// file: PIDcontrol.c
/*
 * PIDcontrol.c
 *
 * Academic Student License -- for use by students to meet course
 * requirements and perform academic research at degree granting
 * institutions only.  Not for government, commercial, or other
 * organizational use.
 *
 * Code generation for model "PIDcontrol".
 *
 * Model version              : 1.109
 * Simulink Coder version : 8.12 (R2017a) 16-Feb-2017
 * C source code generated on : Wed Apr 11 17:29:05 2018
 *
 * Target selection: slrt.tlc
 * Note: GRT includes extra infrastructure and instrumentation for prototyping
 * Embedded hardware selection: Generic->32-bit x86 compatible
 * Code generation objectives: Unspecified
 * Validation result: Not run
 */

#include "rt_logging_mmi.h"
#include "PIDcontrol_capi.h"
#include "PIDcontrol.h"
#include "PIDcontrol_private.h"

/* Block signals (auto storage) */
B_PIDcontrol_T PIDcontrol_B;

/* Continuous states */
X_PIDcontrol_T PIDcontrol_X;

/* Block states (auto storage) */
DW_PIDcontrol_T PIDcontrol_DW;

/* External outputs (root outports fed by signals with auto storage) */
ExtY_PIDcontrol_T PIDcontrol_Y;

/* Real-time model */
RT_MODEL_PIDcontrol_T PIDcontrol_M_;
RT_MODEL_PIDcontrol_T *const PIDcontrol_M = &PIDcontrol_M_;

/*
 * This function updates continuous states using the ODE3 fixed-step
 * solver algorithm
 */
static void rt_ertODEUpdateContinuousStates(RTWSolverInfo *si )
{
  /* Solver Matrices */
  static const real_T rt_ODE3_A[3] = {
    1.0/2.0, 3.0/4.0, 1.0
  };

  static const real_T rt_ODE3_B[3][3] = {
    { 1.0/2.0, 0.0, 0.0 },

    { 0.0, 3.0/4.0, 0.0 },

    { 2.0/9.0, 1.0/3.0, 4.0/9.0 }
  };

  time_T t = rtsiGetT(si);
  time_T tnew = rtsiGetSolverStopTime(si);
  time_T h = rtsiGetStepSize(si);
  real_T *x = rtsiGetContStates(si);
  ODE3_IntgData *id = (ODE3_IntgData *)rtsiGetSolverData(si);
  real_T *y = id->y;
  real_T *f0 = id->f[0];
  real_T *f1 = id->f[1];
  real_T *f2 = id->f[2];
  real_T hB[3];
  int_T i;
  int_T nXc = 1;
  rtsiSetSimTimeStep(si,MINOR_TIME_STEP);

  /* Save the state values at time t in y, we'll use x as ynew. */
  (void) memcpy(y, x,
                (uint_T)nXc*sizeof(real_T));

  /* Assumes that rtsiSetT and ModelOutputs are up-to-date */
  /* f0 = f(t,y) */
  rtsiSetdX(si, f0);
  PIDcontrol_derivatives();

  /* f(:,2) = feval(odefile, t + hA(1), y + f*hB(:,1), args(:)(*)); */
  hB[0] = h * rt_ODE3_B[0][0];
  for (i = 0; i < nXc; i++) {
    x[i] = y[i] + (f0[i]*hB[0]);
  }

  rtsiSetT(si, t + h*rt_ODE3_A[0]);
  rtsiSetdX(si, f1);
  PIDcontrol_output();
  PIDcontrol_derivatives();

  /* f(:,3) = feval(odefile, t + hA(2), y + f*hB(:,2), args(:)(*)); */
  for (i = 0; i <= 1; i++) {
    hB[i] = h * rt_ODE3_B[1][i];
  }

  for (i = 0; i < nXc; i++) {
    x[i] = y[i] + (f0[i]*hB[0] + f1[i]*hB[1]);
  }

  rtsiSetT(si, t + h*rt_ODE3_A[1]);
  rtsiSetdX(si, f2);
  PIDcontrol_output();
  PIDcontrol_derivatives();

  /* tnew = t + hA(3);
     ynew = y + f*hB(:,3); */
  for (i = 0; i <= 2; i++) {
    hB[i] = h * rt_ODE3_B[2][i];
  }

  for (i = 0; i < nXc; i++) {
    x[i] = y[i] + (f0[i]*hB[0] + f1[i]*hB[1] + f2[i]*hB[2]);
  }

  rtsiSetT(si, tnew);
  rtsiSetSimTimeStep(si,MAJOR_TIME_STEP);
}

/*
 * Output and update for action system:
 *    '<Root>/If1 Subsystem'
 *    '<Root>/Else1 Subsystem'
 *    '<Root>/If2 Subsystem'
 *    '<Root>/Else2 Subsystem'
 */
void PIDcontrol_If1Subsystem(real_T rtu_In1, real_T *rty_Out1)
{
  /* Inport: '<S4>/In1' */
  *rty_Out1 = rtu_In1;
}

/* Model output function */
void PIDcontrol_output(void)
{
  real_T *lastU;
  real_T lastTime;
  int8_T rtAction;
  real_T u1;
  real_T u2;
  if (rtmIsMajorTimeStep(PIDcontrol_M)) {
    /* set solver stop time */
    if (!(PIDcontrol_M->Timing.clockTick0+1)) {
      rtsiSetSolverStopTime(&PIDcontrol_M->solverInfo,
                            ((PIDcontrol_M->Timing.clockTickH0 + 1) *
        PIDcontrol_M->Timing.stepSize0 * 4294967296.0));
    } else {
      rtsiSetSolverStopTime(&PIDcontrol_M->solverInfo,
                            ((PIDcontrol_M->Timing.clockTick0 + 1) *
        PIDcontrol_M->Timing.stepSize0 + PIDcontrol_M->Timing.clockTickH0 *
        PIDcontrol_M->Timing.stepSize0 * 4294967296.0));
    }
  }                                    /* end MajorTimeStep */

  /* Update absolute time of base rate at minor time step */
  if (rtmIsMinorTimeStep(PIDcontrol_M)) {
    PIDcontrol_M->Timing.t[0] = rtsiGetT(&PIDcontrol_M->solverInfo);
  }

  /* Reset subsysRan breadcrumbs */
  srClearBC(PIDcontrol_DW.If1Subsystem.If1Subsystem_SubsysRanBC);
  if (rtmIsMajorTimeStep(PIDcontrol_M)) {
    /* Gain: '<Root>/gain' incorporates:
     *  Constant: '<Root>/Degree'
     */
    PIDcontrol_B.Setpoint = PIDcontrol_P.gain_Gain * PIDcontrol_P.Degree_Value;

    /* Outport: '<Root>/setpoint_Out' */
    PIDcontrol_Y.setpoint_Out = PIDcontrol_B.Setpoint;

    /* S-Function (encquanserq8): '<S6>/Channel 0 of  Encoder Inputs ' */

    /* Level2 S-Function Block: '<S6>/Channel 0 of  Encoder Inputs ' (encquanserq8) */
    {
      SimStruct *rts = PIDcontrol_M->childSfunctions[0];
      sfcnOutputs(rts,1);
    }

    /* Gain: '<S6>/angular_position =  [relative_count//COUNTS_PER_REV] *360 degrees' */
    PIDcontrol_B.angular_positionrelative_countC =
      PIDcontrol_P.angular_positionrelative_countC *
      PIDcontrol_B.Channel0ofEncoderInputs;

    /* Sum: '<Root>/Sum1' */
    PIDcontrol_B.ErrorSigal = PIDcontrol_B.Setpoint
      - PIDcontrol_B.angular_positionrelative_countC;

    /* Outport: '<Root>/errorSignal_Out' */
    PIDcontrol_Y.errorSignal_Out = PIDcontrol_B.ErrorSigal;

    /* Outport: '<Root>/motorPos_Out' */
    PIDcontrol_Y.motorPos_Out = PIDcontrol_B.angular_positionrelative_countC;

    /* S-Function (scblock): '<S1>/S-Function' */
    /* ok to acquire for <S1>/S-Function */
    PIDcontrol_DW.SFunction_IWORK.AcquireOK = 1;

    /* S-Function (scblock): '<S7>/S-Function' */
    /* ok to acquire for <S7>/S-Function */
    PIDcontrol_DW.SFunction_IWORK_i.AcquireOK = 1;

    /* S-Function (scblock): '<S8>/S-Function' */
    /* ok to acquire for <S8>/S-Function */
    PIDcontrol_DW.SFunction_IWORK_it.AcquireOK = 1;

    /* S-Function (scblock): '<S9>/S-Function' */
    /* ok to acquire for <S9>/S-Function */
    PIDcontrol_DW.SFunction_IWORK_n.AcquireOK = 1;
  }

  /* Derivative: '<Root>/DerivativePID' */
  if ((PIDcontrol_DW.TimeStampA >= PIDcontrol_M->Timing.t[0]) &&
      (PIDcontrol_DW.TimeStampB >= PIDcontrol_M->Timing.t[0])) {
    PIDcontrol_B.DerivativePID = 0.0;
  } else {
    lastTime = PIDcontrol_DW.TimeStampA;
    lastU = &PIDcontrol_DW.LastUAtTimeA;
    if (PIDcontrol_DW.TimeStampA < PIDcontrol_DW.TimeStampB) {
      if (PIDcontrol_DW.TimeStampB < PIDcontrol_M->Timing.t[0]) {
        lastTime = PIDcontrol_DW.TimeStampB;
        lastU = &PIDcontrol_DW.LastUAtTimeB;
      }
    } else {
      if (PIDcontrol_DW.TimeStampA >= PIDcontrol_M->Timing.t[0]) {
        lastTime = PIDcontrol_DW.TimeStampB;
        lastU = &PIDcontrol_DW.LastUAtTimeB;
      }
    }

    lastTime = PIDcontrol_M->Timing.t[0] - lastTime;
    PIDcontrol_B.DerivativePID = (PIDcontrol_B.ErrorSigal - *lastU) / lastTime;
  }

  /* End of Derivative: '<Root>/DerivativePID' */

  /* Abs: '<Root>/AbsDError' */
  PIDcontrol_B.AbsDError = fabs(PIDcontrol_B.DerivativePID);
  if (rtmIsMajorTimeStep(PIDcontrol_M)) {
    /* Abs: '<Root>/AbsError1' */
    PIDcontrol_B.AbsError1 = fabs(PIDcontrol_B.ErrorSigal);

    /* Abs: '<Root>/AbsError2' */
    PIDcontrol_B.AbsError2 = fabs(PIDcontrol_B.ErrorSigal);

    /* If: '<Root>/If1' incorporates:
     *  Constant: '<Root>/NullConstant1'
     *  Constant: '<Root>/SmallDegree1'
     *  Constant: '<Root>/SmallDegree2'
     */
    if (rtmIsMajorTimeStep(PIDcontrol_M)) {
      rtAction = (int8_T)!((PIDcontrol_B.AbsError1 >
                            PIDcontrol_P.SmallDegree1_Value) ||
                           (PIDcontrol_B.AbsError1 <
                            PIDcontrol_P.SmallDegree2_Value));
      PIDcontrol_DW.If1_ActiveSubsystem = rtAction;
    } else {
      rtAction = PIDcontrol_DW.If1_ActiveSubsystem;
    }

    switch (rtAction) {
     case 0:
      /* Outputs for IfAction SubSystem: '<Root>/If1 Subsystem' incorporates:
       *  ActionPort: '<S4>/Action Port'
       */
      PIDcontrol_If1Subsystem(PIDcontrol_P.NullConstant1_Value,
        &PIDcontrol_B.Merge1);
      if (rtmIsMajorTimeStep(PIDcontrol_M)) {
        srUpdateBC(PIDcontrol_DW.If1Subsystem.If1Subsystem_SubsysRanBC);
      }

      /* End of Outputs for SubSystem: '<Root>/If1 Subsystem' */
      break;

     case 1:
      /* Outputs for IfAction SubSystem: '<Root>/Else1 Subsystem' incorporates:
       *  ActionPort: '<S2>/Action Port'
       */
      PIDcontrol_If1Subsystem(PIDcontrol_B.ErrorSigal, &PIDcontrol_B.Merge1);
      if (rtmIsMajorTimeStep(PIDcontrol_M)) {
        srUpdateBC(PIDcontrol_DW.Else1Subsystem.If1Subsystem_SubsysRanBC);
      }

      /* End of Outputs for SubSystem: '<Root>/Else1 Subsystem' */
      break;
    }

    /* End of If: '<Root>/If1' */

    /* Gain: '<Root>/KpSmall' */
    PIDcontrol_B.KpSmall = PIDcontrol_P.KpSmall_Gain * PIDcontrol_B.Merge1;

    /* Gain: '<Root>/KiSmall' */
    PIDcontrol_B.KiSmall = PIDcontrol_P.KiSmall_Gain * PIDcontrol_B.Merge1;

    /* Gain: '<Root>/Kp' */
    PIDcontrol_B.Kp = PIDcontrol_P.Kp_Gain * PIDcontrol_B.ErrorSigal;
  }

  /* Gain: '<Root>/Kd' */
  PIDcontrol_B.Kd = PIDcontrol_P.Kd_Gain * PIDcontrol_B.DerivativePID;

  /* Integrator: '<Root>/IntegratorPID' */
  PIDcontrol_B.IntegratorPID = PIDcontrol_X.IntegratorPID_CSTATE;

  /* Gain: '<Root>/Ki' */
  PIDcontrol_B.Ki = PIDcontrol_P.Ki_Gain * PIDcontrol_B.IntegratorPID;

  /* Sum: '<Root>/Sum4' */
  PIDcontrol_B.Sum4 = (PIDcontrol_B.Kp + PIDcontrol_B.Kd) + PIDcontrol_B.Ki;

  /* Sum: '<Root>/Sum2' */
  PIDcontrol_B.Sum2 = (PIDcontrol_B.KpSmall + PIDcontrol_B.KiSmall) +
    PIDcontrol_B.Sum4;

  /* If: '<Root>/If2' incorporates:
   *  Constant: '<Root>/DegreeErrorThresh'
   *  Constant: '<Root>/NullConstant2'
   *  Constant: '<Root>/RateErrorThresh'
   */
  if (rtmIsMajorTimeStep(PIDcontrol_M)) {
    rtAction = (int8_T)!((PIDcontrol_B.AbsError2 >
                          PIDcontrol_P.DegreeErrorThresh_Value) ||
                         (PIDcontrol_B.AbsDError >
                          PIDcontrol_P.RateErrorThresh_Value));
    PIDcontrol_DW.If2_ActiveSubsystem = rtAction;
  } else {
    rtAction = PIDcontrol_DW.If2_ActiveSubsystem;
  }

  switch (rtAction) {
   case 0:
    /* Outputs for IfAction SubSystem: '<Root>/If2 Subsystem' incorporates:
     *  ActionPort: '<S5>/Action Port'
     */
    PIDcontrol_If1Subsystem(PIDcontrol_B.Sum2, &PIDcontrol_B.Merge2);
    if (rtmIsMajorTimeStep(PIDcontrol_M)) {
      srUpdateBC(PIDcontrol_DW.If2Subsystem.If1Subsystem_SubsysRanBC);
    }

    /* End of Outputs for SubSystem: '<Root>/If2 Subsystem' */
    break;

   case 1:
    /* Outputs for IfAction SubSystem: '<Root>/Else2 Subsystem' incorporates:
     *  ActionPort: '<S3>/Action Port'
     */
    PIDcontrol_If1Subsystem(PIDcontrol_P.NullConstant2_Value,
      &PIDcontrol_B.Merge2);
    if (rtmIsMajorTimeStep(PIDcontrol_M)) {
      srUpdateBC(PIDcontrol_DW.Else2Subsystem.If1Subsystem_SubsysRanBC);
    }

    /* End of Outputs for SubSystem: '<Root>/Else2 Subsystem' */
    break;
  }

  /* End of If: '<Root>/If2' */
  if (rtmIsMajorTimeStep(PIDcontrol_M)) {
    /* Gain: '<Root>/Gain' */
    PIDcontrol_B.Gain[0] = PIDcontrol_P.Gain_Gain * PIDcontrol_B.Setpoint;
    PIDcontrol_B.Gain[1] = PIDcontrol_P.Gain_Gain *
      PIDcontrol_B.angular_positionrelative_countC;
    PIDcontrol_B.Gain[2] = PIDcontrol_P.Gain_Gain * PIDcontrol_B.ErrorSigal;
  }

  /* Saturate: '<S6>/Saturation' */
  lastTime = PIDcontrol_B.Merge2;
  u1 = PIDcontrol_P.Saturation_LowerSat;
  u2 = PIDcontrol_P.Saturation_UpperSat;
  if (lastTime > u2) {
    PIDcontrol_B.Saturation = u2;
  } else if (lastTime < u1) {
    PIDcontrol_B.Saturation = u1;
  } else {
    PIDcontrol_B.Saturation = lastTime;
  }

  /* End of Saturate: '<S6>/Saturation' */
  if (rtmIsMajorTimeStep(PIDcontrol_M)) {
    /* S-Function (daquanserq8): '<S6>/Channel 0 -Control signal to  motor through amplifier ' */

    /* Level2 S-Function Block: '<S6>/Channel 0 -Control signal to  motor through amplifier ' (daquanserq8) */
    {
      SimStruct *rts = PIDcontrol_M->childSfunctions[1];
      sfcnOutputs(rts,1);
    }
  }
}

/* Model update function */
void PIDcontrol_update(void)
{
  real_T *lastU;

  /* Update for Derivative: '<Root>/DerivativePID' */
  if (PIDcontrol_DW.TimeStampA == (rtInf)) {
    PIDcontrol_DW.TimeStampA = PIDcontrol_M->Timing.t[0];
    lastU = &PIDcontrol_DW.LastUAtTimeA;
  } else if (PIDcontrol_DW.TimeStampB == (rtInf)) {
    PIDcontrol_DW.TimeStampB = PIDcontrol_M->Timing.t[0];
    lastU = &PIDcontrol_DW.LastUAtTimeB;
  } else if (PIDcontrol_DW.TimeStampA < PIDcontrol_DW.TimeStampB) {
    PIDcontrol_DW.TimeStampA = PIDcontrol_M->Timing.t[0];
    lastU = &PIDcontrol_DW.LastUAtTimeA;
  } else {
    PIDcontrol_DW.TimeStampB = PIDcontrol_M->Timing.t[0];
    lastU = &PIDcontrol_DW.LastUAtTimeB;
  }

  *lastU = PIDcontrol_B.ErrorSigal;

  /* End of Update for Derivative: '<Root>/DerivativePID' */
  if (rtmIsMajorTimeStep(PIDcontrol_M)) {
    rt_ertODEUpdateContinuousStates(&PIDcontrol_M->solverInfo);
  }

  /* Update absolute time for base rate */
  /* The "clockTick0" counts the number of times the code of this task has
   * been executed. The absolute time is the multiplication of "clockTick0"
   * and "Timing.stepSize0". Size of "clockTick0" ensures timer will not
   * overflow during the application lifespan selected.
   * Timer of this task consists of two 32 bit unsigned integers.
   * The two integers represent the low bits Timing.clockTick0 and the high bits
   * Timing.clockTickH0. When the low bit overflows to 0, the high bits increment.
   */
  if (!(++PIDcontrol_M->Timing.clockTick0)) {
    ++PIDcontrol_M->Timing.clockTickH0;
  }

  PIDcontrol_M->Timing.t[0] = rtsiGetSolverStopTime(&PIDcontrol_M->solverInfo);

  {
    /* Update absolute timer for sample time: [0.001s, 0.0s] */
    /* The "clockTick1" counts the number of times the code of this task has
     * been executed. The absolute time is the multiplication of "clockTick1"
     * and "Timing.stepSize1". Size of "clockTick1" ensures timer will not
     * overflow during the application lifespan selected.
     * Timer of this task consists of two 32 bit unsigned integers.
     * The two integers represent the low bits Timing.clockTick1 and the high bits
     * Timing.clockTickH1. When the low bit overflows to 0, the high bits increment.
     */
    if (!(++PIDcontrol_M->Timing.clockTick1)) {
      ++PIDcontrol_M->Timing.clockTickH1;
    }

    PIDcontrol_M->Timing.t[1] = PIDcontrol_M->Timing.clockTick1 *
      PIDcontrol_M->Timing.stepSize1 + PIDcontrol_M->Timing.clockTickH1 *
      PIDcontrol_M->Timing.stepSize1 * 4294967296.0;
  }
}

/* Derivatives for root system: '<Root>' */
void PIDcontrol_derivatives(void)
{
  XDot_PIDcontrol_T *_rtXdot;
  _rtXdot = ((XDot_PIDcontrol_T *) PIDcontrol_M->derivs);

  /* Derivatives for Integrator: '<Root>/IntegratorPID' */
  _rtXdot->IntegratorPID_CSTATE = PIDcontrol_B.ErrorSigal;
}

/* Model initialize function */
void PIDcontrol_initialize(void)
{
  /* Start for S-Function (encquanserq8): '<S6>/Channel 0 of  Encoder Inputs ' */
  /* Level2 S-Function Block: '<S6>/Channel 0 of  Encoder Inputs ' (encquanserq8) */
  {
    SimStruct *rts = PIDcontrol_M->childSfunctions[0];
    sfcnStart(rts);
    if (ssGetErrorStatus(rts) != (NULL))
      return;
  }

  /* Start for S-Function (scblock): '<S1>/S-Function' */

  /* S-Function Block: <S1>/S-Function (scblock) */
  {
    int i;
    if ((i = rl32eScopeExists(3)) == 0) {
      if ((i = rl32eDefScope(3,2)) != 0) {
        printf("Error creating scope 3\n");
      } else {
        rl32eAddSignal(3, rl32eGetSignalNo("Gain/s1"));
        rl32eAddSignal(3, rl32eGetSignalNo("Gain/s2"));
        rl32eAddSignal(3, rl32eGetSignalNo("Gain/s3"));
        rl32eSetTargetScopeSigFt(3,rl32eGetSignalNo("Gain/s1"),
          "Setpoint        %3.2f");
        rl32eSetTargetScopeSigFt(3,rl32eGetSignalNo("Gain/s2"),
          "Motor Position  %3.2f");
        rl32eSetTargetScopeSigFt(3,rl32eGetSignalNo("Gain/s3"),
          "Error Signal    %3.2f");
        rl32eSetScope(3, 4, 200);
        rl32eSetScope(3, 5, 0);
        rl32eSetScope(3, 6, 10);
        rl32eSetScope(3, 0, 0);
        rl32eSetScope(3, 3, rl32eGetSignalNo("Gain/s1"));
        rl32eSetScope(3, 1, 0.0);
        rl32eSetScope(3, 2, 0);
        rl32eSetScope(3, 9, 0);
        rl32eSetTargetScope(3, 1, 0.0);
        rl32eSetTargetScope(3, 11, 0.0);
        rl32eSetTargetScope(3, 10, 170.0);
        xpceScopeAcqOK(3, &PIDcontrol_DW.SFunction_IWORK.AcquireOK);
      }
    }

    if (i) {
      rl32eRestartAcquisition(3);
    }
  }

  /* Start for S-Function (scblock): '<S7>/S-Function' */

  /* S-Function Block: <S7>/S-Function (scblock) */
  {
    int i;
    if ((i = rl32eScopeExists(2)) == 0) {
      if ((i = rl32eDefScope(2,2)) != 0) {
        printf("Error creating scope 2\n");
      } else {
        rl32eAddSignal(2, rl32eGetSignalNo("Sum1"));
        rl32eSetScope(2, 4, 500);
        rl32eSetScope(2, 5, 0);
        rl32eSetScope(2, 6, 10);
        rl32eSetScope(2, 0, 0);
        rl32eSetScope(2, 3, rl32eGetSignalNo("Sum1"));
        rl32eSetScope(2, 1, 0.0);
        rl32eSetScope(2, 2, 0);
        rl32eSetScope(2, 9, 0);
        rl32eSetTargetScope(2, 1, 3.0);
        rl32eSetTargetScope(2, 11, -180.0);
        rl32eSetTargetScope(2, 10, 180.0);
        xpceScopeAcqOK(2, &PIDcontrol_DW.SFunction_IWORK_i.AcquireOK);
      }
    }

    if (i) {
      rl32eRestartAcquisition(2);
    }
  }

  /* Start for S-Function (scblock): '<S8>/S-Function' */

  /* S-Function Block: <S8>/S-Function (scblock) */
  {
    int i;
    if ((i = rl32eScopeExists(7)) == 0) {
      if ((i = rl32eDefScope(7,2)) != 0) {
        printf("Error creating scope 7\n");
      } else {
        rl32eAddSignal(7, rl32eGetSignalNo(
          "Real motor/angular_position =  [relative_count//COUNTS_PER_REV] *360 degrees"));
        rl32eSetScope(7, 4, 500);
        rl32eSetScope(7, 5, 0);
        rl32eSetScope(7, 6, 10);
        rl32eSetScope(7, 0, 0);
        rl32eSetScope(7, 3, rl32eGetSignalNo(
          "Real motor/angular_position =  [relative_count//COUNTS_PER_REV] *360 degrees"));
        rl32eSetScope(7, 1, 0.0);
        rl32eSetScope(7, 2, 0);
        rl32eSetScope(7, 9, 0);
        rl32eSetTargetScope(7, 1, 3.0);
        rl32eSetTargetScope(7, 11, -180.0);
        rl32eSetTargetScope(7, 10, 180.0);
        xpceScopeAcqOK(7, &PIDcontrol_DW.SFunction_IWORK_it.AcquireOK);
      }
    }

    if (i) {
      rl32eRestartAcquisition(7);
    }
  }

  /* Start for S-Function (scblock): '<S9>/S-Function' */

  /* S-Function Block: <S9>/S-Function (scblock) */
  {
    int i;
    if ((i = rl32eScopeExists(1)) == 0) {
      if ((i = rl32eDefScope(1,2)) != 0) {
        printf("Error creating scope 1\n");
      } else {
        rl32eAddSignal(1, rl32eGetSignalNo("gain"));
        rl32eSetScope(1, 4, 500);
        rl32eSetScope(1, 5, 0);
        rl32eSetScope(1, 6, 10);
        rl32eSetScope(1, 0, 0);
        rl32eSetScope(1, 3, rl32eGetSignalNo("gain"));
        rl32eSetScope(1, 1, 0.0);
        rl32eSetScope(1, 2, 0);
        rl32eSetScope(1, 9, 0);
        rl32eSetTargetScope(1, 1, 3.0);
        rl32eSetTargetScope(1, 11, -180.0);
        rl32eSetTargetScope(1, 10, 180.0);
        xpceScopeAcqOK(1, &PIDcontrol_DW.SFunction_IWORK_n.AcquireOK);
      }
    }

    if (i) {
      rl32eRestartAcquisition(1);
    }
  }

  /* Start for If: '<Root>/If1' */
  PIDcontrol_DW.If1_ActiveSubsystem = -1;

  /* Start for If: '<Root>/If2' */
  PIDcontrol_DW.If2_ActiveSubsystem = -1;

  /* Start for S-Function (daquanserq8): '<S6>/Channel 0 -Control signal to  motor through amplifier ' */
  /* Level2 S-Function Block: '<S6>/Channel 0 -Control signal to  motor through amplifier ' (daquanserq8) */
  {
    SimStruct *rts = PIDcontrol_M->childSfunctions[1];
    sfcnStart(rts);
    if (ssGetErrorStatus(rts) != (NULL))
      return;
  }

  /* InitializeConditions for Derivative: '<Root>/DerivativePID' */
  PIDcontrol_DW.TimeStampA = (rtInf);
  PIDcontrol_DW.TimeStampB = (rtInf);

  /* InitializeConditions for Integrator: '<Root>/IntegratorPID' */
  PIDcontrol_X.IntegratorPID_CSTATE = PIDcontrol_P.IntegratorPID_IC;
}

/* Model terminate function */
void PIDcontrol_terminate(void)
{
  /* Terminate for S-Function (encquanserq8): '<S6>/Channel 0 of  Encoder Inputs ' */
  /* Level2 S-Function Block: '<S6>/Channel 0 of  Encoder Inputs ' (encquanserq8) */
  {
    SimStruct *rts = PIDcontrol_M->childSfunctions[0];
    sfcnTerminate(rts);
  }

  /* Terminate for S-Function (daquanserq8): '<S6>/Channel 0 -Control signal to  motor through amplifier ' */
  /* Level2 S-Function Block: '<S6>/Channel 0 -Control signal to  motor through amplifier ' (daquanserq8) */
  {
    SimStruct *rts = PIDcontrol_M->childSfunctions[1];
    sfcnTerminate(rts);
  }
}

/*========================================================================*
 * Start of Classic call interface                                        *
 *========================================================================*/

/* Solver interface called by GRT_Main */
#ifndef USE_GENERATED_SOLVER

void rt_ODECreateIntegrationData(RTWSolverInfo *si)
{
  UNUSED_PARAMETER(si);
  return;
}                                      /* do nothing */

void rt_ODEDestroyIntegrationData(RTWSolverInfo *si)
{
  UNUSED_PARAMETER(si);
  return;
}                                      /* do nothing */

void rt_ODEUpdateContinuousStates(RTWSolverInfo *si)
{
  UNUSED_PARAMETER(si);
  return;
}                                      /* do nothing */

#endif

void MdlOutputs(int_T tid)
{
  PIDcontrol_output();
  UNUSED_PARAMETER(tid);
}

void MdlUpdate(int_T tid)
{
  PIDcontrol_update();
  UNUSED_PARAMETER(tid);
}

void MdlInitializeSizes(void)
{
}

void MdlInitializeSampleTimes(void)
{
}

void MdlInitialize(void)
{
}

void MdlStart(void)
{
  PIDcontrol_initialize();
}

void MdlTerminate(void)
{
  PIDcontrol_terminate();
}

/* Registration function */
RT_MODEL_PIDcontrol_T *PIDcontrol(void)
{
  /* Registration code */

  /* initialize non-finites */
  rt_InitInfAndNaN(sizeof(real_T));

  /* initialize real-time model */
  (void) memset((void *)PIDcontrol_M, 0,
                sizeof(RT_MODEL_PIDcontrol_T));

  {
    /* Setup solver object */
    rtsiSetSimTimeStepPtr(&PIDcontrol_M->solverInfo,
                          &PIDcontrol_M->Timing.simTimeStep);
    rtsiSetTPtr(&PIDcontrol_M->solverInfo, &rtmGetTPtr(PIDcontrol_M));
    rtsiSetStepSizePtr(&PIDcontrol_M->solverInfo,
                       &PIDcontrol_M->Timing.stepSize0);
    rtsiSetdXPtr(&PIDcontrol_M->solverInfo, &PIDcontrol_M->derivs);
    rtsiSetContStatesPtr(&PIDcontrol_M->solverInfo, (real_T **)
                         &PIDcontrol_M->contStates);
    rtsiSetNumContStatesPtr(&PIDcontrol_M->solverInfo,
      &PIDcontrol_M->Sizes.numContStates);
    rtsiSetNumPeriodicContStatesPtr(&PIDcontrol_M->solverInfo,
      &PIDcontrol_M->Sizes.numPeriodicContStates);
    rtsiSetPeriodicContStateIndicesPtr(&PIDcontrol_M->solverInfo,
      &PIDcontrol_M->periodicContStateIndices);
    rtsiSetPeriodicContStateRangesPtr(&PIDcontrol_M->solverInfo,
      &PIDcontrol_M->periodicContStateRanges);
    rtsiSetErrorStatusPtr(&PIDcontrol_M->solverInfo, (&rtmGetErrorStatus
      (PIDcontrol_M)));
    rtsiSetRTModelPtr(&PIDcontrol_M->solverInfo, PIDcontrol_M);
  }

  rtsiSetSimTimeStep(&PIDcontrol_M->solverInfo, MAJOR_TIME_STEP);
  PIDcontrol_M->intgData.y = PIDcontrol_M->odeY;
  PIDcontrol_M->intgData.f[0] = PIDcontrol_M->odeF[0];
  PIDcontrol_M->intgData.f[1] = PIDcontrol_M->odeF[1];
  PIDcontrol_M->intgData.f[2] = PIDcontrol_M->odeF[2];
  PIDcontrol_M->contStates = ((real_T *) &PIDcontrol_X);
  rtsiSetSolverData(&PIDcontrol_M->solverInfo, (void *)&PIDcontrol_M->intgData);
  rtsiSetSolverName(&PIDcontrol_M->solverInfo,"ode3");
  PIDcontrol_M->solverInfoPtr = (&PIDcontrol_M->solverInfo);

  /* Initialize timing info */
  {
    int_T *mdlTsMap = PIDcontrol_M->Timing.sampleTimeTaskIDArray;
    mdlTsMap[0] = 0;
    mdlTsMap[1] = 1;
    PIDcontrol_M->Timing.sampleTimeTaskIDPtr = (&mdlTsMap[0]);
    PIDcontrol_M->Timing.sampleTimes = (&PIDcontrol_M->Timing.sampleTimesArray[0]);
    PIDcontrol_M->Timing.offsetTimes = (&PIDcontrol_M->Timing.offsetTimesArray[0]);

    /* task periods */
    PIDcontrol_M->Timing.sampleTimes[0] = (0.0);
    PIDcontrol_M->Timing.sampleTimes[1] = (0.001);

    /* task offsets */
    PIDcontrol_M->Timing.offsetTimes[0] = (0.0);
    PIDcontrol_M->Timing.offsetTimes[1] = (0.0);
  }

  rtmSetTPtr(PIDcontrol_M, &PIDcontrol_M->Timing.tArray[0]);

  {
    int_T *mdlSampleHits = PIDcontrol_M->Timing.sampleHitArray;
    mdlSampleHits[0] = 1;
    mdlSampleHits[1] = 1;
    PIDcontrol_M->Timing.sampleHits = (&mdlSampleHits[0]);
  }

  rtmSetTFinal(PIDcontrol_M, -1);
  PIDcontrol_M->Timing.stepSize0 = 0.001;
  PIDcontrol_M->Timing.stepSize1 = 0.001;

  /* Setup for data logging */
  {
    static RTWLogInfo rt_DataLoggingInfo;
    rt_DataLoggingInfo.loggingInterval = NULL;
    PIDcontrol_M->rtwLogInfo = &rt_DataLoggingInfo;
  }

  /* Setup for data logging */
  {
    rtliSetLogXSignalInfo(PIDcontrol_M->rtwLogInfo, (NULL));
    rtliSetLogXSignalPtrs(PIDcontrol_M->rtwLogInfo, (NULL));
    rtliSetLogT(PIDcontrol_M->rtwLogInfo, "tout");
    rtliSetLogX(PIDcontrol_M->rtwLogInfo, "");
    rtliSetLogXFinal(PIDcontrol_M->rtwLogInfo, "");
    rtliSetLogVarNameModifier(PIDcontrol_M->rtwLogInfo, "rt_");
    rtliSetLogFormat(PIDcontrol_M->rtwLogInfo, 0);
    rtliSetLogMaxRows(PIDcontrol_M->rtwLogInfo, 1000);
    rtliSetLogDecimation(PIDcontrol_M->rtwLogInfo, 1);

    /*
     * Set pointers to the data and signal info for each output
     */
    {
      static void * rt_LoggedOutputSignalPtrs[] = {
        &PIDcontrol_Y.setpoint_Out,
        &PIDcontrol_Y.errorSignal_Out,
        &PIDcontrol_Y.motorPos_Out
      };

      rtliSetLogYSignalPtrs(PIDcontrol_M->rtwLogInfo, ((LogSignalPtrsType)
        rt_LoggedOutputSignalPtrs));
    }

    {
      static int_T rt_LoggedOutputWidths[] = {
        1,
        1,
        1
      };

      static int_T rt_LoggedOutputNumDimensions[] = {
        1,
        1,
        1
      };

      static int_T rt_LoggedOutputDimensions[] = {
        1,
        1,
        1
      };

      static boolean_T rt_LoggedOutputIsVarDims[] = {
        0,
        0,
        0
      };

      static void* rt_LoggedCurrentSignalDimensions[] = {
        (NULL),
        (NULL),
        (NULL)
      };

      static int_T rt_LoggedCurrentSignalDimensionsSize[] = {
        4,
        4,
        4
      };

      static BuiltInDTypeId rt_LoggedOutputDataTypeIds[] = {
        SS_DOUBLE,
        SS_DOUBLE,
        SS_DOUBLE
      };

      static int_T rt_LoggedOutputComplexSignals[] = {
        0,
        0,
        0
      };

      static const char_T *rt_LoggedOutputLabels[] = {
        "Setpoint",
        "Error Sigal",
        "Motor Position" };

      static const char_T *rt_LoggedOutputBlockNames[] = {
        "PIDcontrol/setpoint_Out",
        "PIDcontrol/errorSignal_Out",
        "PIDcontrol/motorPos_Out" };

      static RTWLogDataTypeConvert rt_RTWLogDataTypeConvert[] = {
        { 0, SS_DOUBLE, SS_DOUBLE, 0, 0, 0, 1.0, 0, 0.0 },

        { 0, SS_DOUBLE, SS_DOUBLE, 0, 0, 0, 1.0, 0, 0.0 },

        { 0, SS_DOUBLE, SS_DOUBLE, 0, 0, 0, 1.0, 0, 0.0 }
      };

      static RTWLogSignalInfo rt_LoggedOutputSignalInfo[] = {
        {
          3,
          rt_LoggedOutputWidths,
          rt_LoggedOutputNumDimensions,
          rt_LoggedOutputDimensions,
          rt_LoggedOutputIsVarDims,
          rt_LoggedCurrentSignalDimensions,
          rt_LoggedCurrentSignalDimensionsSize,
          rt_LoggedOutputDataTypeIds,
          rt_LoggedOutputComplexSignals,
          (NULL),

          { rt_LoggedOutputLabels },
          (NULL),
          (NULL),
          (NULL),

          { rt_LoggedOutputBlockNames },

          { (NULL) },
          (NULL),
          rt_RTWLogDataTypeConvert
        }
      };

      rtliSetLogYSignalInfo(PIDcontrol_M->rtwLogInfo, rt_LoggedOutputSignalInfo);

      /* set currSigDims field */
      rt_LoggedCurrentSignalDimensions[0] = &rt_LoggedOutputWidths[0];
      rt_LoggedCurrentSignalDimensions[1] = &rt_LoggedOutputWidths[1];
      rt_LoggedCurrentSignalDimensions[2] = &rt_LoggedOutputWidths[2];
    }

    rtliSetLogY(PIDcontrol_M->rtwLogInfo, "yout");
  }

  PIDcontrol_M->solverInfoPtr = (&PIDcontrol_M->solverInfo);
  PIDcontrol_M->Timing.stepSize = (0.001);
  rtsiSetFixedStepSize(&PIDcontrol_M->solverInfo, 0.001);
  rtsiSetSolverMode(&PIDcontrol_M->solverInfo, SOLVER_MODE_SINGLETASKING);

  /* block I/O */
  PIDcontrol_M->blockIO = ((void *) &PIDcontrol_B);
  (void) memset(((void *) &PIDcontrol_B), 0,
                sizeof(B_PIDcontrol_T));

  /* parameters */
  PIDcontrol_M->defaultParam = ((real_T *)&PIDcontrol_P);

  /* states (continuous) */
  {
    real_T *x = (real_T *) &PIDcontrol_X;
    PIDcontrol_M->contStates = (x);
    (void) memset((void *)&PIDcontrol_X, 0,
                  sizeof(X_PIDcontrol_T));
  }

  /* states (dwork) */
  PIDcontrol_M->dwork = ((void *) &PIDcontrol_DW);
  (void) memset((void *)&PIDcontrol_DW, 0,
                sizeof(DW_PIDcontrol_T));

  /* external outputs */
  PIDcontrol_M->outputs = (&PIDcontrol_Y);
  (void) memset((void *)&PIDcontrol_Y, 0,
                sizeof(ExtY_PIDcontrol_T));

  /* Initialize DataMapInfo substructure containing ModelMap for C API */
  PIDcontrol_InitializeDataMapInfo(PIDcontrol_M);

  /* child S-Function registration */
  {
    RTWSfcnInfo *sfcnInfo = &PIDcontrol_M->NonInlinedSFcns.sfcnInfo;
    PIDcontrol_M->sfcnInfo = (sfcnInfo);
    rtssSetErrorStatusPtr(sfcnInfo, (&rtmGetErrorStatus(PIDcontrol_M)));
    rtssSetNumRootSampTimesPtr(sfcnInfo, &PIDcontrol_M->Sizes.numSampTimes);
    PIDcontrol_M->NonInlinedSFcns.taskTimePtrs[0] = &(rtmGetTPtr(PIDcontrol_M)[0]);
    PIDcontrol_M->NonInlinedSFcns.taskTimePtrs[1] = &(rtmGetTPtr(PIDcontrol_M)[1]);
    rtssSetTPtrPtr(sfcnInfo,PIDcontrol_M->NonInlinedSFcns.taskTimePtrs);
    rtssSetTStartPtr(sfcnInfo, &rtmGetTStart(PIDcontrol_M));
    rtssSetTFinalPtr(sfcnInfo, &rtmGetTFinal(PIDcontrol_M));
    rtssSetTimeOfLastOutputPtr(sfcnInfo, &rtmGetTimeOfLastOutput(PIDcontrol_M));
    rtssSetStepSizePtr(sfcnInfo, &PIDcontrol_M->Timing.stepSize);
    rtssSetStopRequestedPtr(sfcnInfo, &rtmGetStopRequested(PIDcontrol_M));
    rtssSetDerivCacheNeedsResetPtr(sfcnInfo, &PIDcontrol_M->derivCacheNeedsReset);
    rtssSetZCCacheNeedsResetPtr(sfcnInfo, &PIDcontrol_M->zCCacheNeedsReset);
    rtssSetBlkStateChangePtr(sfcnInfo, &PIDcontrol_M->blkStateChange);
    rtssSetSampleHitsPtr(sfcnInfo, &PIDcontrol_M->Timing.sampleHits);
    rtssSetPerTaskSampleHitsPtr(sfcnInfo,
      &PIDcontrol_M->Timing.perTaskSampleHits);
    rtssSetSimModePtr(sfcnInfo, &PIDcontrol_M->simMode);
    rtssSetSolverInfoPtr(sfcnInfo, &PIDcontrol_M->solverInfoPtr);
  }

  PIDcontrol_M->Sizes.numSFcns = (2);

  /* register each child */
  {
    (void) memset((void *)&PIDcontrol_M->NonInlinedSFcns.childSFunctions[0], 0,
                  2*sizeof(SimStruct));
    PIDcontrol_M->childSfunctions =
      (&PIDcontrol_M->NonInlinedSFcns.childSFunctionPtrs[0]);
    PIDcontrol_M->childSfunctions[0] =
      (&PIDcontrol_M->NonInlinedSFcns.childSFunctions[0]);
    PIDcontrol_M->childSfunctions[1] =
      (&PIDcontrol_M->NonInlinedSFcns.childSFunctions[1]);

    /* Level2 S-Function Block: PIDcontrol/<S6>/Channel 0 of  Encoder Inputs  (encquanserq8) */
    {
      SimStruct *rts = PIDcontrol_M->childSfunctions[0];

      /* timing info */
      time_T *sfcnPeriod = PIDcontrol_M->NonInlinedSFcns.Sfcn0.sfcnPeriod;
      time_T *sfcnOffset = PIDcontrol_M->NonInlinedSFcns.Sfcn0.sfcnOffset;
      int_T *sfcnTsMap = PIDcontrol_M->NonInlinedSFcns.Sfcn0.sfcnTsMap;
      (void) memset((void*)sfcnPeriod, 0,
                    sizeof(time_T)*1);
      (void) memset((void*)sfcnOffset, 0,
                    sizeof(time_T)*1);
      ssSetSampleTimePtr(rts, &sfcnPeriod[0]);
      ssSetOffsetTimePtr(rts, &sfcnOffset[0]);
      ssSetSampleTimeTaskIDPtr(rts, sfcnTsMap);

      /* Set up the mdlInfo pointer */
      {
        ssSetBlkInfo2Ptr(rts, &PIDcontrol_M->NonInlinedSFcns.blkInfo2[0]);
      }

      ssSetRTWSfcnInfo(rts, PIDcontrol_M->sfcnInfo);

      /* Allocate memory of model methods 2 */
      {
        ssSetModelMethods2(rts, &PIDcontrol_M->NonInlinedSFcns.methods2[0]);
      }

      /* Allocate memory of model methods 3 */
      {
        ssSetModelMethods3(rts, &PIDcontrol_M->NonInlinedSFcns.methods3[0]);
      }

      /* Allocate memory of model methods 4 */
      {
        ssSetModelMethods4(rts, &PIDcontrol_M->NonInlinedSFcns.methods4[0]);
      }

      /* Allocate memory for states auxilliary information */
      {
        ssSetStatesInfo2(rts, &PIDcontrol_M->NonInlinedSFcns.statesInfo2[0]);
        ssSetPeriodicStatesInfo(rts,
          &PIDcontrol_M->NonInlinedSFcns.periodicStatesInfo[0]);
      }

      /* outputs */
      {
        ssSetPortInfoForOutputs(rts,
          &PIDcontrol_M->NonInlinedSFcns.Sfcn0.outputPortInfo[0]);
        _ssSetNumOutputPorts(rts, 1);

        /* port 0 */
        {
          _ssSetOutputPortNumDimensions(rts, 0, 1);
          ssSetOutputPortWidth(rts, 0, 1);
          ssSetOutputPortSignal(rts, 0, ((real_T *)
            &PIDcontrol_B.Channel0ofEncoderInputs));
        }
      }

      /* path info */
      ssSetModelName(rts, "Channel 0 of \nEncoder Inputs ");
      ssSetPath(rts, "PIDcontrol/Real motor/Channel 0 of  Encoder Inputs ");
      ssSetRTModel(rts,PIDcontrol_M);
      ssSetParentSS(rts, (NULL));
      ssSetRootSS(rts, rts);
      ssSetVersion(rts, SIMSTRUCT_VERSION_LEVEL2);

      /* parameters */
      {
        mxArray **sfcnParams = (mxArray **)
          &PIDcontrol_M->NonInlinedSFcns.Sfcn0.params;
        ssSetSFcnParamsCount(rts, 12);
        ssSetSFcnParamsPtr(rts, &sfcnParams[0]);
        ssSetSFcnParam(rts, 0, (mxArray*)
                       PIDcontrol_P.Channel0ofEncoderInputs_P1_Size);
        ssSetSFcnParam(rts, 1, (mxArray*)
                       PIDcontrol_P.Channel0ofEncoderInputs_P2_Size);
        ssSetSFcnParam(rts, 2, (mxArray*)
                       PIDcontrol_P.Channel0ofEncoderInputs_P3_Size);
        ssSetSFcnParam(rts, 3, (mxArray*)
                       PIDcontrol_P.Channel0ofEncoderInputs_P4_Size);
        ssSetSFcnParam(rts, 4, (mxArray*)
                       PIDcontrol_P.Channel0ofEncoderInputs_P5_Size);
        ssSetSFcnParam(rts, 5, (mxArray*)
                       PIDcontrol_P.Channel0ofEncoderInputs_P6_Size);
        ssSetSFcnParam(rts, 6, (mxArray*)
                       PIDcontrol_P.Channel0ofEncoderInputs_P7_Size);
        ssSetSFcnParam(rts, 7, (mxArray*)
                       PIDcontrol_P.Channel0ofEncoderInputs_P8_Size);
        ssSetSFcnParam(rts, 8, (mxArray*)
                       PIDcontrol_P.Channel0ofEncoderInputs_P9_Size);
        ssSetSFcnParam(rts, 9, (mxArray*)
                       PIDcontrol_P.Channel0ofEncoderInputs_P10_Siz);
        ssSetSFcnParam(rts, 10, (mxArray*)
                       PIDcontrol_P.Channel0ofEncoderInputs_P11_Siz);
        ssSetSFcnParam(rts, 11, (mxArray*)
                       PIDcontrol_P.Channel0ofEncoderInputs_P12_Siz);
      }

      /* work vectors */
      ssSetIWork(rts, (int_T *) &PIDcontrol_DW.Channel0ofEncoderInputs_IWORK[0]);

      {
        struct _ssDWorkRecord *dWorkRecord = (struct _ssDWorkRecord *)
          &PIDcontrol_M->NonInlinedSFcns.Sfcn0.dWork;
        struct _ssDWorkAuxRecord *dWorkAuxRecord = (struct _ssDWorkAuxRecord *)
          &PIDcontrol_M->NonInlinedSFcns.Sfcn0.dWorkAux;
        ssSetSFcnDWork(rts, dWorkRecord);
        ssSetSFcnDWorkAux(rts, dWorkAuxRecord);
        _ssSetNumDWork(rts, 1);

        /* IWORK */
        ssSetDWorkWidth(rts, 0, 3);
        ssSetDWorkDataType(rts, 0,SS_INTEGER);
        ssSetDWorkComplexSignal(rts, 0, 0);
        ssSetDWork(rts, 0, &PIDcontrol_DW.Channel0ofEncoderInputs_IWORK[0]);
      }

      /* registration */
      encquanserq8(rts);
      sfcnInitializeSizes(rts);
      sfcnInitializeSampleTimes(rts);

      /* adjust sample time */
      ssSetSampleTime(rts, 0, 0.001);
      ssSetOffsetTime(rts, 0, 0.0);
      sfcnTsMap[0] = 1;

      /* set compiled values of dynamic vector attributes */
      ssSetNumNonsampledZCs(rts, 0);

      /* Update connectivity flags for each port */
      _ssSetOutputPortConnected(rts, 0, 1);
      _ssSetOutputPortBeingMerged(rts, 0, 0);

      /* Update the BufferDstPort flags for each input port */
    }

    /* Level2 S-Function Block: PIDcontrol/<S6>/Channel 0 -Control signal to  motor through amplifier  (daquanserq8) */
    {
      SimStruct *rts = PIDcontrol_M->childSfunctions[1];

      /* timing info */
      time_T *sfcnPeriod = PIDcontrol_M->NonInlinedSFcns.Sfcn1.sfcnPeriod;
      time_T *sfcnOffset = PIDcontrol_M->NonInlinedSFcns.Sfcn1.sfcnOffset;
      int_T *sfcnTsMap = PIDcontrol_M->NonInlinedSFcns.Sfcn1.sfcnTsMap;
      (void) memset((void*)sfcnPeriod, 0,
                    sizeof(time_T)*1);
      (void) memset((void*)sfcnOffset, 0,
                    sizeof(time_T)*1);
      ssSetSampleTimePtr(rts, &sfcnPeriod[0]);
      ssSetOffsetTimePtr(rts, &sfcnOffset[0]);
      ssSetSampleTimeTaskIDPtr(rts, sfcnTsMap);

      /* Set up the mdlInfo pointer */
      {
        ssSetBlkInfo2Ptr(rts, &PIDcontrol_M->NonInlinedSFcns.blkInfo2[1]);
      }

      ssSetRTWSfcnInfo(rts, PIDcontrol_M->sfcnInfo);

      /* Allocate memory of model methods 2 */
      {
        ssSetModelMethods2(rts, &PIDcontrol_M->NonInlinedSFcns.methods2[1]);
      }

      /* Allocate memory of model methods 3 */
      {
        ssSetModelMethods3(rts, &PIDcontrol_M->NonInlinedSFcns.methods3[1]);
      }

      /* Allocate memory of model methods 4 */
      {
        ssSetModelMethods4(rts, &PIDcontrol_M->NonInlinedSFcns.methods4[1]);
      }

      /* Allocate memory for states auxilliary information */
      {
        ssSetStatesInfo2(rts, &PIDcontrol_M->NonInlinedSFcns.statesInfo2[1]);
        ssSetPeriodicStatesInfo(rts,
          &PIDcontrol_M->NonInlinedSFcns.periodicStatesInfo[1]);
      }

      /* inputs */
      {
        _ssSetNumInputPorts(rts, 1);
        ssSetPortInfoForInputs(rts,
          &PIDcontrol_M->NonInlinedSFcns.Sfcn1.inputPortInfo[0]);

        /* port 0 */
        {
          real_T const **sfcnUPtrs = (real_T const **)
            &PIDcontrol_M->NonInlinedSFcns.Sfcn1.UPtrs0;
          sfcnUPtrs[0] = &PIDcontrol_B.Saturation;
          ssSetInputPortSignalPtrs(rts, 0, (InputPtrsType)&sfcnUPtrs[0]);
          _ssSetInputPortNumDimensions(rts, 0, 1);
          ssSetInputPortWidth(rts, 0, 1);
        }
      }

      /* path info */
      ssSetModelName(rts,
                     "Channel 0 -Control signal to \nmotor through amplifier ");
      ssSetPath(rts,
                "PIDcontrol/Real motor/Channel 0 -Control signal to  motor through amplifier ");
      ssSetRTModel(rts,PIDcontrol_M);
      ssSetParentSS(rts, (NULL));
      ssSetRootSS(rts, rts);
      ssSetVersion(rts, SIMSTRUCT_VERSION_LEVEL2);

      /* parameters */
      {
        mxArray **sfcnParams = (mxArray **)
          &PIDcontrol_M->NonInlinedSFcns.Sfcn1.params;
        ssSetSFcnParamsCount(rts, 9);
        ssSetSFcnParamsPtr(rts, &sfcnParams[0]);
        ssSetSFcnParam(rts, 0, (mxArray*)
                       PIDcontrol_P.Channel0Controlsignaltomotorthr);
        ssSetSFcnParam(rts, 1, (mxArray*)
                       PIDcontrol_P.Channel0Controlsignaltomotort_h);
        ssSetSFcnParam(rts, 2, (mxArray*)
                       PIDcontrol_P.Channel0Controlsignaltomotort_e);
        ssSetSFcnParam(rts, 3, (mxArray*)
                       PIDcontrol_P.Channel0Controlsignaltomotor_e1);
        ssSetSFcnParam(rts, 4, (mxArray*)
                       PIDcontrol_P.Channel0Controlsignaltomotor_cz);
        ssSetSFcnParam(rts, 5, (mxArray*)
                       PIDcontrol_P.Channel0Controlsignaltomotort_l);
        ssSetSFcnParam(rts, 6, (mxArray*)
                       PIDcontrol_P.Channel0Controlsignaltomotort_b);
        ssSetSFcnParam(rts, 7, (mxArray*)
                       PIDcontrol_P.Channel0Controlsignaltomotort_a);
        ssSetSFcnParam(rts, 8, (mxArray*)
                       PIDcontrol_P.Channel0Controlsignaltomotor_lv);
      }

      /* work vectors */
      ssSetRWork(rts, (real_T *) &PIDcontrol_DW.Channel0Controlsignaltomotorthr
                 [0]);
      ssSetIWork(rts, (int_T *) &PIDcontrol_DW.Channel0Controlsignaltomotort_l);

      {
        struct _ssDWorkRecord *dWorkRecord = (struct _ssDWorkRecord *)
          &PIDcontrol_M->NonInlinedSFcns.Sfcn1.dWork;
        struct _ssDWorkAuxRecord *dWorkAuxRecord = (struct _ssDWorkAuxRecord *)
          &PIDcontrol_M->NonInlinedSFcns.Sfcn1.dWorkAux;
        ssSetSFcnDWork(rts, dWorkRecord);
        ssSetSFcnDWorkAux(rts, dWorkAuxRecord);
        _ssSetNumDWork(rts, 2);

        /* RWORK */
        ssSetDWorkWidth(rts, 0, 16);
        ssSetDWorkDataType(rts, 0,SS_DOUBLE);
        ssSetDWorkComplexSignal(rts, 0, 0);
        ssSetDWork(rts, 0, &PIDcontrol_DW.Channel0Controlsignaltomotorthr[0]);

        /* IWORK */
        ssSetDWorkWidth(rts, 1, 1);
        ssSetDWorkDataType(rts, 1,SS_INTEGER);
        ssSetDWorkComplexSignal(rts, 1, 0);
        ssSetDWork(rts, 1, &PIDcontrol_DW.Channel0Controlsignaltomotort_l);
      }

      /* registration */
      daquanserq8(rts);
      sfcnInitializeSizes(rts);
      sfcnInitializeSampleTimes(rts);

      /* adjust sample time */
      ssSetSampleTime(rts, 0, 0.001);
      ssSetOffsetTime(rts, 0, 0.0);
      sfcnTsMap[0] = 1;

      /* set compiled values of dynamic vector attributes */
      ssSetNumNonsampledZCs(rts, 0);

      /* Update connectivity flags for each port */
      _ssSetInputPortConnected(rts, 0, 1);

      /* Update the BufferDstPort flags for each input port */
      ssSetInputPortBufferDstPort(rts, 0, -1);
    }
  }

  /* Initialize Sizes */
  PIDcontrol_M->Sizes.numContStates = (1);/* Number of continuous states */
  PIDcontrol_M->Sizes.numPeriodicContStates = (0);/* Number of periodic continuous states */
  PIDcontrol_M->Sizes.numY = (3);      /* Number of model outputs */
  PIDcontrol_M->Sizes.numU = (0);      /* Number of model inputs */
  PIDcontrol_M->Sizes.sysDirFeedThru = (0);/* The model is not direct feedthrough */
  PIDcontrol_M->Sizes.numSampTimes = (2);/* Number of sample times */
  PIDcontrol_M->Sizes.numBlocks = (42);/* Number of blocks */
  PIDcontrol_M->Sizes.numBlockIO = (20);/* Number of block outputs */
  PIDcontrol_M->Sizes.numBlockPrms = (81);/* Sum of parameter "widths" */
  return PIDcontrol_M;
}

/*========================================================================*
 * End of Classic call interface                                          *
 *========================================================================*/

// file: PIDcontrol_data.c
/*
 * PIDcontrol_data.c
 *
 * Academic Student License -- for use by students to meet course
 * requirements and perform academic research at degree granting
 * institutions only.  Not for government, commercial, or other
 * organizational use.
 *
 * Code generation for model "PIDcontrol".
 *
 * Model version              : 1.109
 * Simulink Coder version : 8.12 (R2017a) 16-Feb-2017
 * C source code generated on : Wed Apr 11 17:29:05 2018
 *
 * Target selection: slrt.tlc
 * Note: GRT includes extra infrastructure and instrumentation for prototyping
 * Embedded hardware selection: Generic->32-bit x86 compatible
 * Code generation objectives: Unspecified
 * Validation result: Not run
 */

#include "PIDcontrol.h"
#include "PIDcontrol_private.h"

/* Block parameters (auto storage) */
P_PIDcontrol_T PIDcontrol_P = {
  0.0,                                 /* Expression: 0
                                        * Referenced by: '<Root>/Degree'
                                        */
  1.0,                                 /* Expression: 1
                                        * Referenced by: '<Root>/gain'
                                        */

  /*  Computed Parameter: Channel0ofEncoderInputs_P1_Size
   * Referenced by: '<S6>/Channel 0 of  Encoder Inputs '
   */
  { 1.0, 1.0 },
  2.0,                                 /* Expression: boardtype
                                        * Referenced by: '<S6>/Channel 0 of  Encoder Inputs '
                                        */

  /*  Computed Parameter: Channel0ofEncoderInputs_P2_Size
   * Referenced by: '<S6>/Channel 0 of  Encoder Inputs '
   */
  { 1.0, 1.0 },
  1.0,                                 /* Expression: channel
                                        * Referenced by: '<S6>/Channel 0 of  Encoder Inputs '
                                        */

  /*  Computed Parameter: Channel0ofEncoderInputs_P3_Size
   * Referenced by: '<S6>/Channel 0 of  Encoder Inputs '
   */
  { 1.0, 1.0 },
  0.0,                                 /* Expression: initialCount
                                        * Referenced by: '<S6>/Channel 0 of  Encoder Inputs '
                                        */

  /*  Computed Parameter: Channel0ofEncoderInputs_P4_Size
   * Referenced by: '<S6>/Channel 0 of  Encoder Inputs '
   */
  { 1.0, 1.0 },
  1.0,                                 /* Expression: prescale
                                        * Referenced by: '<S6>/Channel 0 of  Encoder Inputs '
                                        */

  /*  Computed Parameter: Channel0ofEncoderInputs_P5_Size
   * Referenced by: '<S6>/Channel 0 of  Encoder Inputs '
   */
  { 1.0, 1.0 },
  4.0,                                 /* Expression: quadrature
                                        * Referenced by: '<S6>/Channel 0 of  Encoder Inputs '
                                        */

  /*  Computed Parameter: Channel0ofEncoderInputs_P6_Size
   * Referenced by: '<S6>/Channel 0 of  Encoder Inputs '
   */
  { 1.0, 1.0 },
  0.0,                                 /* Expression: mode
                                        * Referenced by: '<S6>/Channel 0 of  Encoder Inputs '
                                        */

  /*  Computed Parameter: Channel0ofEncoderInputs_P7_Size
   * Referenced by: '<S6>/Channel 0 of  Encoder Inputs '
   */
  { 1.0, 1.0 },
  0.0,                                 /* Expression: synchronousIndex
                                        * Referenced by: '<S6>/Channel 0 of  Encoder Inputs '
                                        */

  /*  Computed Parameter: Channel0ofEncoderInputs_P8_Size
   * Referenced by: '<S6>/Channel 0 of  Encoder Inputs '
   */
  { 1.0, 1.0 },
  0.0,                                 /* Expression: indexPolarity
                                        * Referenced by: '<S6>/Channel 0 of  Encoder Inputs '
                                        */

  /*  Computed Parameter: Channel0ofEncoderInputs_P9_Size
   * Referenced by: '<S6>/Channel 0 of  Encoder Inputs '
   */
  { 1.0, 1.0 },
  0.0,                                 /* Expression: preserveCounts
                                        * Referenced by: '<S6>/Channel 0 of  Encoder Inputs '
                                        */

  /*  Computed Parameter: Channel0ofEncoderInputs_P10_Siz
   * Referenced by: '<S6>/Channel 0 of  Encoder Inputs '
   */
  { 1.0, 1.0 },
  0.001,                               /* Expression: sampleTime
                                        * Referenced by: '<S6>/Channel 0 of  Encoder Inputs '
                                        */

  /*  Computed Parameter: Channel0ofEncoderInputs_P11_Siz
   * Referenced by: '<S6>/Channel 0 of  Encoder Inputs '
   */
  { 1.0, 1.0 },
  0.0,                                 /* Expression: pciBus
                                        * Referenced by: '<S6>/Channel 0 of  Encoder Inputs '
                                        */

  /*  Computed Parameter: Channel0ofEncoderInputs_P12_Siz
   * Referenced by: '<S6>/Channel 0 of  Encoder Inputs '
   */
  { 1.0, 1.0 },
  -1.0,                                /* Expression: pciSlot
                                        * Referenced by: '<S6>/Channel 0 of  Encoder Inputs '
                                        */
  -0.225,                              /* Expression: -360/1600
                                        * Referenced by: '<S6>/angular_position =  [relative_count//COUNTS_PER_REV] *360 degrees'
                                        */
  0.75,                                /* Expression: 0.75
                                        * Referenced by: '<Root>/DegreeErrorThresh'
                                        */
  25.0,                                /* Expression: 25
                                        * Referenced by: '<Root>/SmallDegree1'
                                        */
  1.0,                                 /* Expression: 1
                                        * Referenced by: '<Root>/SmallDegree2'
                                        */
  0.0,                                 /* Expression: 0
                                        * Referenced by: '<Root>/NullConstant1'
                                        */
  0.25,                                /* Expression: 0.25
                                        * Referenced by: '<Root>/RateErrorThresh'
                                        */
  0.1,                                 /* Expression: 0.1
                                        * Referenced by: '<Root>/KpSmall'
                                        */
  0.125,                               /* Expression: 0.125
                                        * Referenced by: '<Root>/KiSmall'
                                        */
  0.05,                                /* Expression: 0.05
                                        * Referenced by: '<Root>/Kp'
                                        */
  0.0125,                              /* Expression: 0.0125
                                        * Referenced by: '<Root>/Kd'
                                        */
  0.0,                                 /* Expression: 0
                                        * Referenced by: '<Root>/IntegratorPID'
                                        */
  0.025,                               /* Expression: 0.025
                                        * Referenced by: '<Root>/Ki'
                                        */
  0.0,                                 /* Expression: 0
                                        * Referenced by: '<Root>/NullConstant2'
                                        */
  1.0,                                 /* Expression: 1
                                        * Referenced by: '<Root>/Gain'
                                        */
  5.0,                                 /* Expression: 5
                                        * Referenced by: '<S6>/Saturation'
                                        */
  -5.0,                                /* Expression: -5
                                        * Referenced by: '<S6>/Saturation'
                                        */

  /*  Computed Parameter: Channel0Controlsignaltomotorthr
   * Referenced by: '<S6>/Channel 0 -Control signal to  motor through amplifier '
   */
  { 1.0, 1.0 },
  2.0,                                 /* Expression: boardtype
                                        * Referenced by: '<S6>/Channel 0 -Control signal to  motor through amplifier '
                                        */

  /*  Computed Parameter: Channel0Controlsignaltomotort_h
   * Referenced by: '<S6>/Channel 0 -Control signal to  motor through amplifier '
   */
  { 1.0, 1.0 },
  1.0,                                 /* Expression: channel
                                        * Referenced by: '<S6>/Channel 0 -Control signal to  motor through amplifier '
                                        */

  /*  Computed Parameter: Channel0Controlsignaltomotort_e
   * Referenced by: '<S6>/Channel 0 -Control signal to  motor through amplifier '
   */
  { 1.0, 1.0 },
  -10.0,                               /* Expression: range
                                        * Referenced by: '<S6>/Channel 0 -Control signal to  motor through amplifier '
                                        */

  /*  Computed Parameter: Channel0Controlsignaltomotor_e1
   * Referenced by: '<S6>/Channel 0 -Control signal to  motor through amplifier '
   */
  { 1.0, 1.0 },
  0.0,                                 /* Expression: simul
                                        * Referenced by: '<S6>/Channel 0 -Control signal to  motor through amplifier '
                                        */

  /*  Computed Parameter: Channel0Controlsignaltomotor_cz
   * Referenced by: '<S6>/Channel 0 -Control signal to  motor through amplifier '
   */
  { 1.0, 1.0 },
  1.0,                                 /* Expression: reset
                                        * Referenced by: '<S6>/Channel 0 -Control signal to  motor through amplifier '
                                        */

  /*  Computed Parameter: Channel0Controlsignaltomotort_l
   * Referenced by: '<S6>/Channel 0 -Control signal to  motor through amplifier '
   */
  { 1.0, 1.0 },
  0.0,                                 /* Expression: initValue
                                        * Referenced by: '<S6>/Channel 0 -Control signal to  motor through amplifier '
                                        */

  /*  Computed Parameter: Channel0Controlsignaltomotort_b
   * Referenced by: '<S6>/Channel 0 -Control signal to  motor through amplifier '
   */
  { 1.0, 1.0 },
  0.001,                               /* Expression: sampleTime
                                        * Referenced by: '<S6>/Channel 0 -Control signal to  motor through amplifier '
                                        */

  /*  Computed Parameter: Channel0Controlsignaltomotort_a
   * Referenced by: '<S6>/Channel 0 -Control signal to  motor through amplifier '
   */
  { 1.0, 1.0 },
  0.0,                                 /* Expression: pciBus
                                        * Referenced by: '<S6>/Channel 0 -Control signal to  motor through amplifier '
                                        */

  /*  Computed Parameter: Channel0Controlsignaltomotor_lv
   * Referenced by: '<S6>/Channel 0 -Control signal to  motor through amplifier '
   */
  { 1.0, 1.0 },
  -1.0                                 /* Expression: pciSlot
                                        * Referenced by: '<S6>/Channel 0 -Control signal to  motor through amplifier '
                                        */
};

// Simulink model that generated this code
simulink model "PIDcontrol"  (Simulink 8.9)
settings: Solver=ode3  StartTime=0.0  StopTime=inf  FixedStep=0.001  RelTol=1e-3  EnableMultiTasking=on
libraries: slrtlib x4, xpcquanserlib x2

== system PIDcontrol ==
  AbsDError : Abs
  AbsError1 : Abs
  AbsError2 : Abs
  Data Display : slrtlib/Displays and Logging/Scope   scopeno=3  scopetype=Target  autostart=on  viewmode=Numerical  formatstr="'Setpoint        %3.2f,Motor Position  %3.2f,Error Signal    %3.2f'"  grid=on  ylimits=[0,170]  nosamples=200  noprepostsamples=0  interleave=10  triggermode=FreeRun  triggersignal=1  trigsignalfromport=off  triggerlevel=0.0  triggerslope=Either  triggerscope=1  triggersample=0  filename=data.dat  mode=Lazy  writesize=512  autorestart=off  dynamicfilemode=off  maxwritefilesize=512*1024^2
  Degree : Constant  Value=0
  DegreeErrorThresh : Constant  Value=0.75
  DerivativePID : Derivative
  Else1 Subsystem : Subsystem  TreatAsAtomicUnit=on
  Else2 Subsystem : Subsystem  TreatAsAtomicUnit=on
  Gain : Gain
  If1 : If  NumInputs=3  IfExpression=u1 > u2 | u1 < u3
  If1 Subsystem : Subsystem  TreatAsAtomicUnit=on
  If2 : If  NumInputs=4  IfExpression=u1 > u2 | u3 > u4
  If2 Subsystem : Subsystem  TreatAsAtomicUnit=on
  IntegratorPID : Integrator
  Kd : Gain  Gain=0.0125
  Ki : Gain  Gain=0.025
  KiSmall : Gain  Gain=0.125
  Kp : Gain  Gain=0.05
  KpSmall : Gain  Gain=0.1
  Merge1 : Merge
  Merge2 : Merge
  Mux : Mux  Inputs=3
  NullConstant1 : Constant  Value=0
  NullConstant2 : Constant  Value=0
  RateErrorThresh : Constant  Value=0.25
  Real motor : Subsystem
  SmallDegree1 : Constant  Value=25
  SmallDegree2 : Constant
  Sum1 : Sum  Inputs=|+-
  Sum2 : Sum  Inputs=||+++
  Sum4 : Sum  Inputs=||+++
  error signal : slrtlib/Displays and Logging/Scope   scopeno=2  scopetype=Target  autostart=on  viewmode=Graphical rolling  formatstr='%15.6f'  grid=on  ylimits=[-180,180]  nosamples=500  noprepostsamples=0  interleave=10  triggermode=FreeRun  triggersignal=1  trigsignalfromport=off  triggerlevel=0.0  triggerslope=Either  triggerscope=1  triggersample=0  filename=data.dat  mode=Lazy  writesize=512  autorestart=off  dynamicfilemode=off  maxwritefilesize=512*1024^2
  gain : Gain
  motor position : slrtlib/Displays and Logging/Scope   scopeno=7  scopetype=Target  autostart=on  viewmode=Graphical rolling  formatstr='%15.6f'  grid=on  ylimits=[-180,180]  nosamples=500  noprepostsamples=0  interleave=10  triggermode=FreeRun  triggersignal=1  trigsignalfromport=off  triggerlevel=0.0  triggerslope=Either  triggerscope=1  triggersample=0  filename=data.dat  mode=Lazy  writesize=512  autorestart=off  dynamicfilemode=off  maxwritefilesize=512*1024^2
  setpoint : slrtlib/Displays and Logging/Scope   scopeno=1  scopetype=Target  autostart=on  viewmode=Graphical rolling  formatstr='%15.6f'  grid=on  ylimits=[-180,180]  nosamples=500  noprepostsamples=0  interleave=10  triggermode=FreeRun  triggersignal=1  trigsignalfromport=off  triggerlevel=0.0  triggerslope=Either  triggerscope=1  triggersample=0  filename=data.dat  mode=Lazy  writesize=512  autorestart=off  dynamicfilemode=off  maxwritefilesize=512*1024^2
  setpoint_Out : Outport
  errorSignal_Out : Outport  Port=2
  motorPos_Out : Outport  Port=3
  wires:
  Kd/1 -> Sum4/2
  DerivativePID/1 -> AbsDError/1, Kd/1
  IntegratorPID/1 -> Ki/1
  Ki/1 -> Sum4/3
  gain/1 -> Sum1/1, Mux/1, setpoint/1, setpoint_Out/1  "Setpoint"
  Degree/1 -> gain/1
  Real motor/1(position in degrees) -> Sum1/2, motor position/1, motorPos_Out/1, Mux/2  "Motor Position"
  Gain/1 -> Data Display/1
  Mux/1 -> Gain/1
  Sum1/1 -> AbsError2/1, Kp/1, DerivativePID/1, IntegratorPID/1, AbsError1/1, Else1 Subsystem/1(In1), error signal/1, Mux/3, errorSignal_Out/1  "Error Sigal"
  Else2 Subsystem/1(Out1) -> Merge2/2
  If2 Subsystem/1(Out1) -> Merge2/1
  NullConstant2/1 -> Else2 Subsystem/1(In1)
  AbsError2/1 -> If2/1
  AbsDError/1 -> If2/3
  DegreeErrorThresh/1 -> If2/2
  RateErrorThresh/1 -> If2/4
  If2/1 -> If2 Subsystem/Action
  If2/2 -> Else2 Subsystem/Action
  Merge2/1 -> Real motor/1(unfiltered  control input)
  Kp/1 -> Sum4/1
  If1/1 -> If1 Subsystem/Action
  If1/2 -> Else1 Subsystem/Action
  Sum2/1 -> If2 Subsystem/1(In1)
  Sum4/1 -> Sum2/3
  KiSmall/1 -> Sum2/2
  KpSmall/1 -> Sum2/1
  If1 Subsystem/1(Out1) -> Merge1/1
  Else1 Subsystem/1(Out1) -> Merge1/2
  Merge1/1 -> KpSmall/1, KiSmall/1
  AbsError1/1 -> If1/1
  NullConstant1/1 -> If1 Subsystem/1(In1)
  SmallDegree2/1 -> If1/3
  SmallDegree1/1 -> If1/2

== system PIDcontrol/Else1 Subsystem ==
  In1 : Inport
  Action Port : ActionPort  ActionType=else
  Out1 : Outport
  wires:
  In1/1 -> Out1/1

== system PIDcontrol/Else2 Subsystem ==
  In1 : Inport
  Action Port : ActionPort  ActionType=else
  Out1 : Outport
  wires:
  In1/1 -> Out1/1

== system PIDcontrol/If1 Subsystem ==
  In1 : Inport
  Action Port : ActionPort  ActionType=then
  Out1 : Outport
  wires:
  In1/1 -> Out1/1

== system PIDcontrol/If2 Subsystem ==
  In1 : Inport
  Action Port : ActionPort  ActionType=then
  Out1 : Outport
  wires:
  In1/1 -> Out1/1

== system PIDcontrol/Real motor ==
  note: Saturation
  note: External connections to and from the motor using the Q4.
      |
      | Encoder feedback is scaled using the modulus and Gain blocks to
      | match the range of the Desired Trajectory input.
      |
      | In this example need to convert the encoder counts to a value between 0 and COUNTS_PER_REV.
      | Further, the count obtained for that revolution needs to be scaled to an angle feedback (between
      | 0 and 360 degrees), which is the purpose of the Gain block.
  unfiltered  control input : Inport
  "Channel 0 -Control signal to  motor through amplifier " : xpcquanserlib/D//A/Q4 DA   channel=[1]  range=[-10]  simul=off  reset=[1]  initValue=[0]  sampleTime=.001  slot=-1
  "Channel 0 of  Encoder Inputs " : xpcquanserlib/Incremental Encoder/Q4 Enc   channel=[1]  initialCount=[0]  prescale=[1]  quadrature=[4]  mode=[0]  synchronousIndex=[0]  indexPolarity=[0]  preserveCounts=[0]  sampleTime=.001  slot=-1
  Saturation : Saturate  UpperLimit=5  LowerLimit=-5
  angular_position =  [relative_count/COUNTS_PER_REV] *360 degrees : Gain  Gain=-360/1600
  position in degrees : Outport
  wires:
  Saturation/1 -> "Channel 0 -Control signal to  motor through amplifier "/1
  angular_position =  [relative_count/COUNTS_PER_REV] *360 degrees/1 -> position in degrees/1
  "Channel 0 of  Encoder Inputs "/1 -> angular_position =  [relative_count/COUNTS_PER_REV] *360 degrees/1
  unfiltered  control input/1 -> Saturation/1
